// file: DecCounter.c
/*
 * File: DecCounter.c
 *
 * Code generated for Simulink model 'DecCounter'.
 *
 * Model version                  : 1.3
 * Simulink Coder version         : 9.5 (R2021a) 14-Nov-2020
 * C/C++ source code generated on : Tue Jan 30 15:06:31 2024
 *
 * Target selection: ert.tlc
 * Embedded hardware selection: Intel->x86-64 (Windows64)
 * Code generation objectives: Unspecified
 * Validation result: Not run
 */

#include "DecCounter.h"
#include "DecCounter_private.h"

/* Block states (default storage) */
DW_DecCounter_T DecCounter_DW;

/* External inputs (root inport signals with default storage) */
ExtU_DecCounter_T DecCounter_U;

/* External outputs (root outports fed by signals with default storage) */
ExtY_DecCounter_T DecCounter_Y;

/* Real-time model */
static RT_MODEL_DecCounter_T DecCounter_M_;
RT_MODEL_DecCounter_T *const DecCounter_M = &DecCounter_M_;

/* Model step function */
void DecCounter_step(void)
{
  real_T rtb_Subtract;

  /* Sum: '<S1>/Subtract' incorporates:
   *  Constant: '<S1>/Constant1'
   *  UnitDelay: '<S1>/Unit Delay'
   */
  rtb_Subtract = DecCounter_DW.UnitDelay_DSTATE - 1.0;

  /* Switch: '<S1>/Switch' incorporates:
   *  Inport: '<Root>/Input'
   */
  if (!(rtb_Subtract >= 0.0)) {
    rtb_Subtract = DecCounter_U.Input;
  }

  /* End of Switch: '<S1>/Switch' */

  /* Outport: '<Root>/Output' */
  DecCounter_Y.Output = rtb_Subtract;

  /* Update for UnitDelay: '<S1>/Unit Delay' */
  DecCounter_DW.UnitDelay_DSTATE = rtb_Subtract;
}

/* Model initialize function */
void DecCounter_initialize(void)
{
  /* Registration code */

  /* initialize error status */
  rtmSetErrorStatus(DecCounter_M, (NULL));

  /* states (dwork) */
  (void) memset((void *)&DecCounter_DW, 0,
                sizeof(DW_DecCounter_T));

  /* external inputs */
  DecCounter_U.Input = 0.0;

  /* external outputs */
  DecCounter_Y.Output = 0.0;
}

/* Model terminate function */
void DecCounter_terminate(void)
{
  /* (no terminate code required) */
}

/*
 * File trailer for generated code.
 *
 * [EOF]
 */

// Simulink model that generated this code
simulink model "DecCounter"  (R2021a)
settings: Solver=FixedStepDiscrete  StartTime=0.0  StopTime=10.0  RelTol=1e-3  EnableMultiTasking=on

== system DecCounter ==
  Input : Inport
  Subsystem : Subsystem
  Output : Outport
  wires:
  Input/1 -> Subsystem/1(In1)
  Subsystem/1(Out1) -> Output/1

== system DecCounter/Subsystem ==
  In1 : Inport
  Constant1 : Constant
  Subtract : Sum  Inputs=-+
  Switch : Switch
  Unit Delay : UnitDelay  SampleTime=-1  HasFrameUpgradeWarning=on
  Out1 : Outport
  wires:
  Switch/1 -> Out1/1, Unit Delay/1
  Constant1/1 -> Subtract/1
  Unit Delay/1 -> Subtract/2
  Subtract/1 -> Switch/2, Switch/1
  In1/1 -> Switch/3
